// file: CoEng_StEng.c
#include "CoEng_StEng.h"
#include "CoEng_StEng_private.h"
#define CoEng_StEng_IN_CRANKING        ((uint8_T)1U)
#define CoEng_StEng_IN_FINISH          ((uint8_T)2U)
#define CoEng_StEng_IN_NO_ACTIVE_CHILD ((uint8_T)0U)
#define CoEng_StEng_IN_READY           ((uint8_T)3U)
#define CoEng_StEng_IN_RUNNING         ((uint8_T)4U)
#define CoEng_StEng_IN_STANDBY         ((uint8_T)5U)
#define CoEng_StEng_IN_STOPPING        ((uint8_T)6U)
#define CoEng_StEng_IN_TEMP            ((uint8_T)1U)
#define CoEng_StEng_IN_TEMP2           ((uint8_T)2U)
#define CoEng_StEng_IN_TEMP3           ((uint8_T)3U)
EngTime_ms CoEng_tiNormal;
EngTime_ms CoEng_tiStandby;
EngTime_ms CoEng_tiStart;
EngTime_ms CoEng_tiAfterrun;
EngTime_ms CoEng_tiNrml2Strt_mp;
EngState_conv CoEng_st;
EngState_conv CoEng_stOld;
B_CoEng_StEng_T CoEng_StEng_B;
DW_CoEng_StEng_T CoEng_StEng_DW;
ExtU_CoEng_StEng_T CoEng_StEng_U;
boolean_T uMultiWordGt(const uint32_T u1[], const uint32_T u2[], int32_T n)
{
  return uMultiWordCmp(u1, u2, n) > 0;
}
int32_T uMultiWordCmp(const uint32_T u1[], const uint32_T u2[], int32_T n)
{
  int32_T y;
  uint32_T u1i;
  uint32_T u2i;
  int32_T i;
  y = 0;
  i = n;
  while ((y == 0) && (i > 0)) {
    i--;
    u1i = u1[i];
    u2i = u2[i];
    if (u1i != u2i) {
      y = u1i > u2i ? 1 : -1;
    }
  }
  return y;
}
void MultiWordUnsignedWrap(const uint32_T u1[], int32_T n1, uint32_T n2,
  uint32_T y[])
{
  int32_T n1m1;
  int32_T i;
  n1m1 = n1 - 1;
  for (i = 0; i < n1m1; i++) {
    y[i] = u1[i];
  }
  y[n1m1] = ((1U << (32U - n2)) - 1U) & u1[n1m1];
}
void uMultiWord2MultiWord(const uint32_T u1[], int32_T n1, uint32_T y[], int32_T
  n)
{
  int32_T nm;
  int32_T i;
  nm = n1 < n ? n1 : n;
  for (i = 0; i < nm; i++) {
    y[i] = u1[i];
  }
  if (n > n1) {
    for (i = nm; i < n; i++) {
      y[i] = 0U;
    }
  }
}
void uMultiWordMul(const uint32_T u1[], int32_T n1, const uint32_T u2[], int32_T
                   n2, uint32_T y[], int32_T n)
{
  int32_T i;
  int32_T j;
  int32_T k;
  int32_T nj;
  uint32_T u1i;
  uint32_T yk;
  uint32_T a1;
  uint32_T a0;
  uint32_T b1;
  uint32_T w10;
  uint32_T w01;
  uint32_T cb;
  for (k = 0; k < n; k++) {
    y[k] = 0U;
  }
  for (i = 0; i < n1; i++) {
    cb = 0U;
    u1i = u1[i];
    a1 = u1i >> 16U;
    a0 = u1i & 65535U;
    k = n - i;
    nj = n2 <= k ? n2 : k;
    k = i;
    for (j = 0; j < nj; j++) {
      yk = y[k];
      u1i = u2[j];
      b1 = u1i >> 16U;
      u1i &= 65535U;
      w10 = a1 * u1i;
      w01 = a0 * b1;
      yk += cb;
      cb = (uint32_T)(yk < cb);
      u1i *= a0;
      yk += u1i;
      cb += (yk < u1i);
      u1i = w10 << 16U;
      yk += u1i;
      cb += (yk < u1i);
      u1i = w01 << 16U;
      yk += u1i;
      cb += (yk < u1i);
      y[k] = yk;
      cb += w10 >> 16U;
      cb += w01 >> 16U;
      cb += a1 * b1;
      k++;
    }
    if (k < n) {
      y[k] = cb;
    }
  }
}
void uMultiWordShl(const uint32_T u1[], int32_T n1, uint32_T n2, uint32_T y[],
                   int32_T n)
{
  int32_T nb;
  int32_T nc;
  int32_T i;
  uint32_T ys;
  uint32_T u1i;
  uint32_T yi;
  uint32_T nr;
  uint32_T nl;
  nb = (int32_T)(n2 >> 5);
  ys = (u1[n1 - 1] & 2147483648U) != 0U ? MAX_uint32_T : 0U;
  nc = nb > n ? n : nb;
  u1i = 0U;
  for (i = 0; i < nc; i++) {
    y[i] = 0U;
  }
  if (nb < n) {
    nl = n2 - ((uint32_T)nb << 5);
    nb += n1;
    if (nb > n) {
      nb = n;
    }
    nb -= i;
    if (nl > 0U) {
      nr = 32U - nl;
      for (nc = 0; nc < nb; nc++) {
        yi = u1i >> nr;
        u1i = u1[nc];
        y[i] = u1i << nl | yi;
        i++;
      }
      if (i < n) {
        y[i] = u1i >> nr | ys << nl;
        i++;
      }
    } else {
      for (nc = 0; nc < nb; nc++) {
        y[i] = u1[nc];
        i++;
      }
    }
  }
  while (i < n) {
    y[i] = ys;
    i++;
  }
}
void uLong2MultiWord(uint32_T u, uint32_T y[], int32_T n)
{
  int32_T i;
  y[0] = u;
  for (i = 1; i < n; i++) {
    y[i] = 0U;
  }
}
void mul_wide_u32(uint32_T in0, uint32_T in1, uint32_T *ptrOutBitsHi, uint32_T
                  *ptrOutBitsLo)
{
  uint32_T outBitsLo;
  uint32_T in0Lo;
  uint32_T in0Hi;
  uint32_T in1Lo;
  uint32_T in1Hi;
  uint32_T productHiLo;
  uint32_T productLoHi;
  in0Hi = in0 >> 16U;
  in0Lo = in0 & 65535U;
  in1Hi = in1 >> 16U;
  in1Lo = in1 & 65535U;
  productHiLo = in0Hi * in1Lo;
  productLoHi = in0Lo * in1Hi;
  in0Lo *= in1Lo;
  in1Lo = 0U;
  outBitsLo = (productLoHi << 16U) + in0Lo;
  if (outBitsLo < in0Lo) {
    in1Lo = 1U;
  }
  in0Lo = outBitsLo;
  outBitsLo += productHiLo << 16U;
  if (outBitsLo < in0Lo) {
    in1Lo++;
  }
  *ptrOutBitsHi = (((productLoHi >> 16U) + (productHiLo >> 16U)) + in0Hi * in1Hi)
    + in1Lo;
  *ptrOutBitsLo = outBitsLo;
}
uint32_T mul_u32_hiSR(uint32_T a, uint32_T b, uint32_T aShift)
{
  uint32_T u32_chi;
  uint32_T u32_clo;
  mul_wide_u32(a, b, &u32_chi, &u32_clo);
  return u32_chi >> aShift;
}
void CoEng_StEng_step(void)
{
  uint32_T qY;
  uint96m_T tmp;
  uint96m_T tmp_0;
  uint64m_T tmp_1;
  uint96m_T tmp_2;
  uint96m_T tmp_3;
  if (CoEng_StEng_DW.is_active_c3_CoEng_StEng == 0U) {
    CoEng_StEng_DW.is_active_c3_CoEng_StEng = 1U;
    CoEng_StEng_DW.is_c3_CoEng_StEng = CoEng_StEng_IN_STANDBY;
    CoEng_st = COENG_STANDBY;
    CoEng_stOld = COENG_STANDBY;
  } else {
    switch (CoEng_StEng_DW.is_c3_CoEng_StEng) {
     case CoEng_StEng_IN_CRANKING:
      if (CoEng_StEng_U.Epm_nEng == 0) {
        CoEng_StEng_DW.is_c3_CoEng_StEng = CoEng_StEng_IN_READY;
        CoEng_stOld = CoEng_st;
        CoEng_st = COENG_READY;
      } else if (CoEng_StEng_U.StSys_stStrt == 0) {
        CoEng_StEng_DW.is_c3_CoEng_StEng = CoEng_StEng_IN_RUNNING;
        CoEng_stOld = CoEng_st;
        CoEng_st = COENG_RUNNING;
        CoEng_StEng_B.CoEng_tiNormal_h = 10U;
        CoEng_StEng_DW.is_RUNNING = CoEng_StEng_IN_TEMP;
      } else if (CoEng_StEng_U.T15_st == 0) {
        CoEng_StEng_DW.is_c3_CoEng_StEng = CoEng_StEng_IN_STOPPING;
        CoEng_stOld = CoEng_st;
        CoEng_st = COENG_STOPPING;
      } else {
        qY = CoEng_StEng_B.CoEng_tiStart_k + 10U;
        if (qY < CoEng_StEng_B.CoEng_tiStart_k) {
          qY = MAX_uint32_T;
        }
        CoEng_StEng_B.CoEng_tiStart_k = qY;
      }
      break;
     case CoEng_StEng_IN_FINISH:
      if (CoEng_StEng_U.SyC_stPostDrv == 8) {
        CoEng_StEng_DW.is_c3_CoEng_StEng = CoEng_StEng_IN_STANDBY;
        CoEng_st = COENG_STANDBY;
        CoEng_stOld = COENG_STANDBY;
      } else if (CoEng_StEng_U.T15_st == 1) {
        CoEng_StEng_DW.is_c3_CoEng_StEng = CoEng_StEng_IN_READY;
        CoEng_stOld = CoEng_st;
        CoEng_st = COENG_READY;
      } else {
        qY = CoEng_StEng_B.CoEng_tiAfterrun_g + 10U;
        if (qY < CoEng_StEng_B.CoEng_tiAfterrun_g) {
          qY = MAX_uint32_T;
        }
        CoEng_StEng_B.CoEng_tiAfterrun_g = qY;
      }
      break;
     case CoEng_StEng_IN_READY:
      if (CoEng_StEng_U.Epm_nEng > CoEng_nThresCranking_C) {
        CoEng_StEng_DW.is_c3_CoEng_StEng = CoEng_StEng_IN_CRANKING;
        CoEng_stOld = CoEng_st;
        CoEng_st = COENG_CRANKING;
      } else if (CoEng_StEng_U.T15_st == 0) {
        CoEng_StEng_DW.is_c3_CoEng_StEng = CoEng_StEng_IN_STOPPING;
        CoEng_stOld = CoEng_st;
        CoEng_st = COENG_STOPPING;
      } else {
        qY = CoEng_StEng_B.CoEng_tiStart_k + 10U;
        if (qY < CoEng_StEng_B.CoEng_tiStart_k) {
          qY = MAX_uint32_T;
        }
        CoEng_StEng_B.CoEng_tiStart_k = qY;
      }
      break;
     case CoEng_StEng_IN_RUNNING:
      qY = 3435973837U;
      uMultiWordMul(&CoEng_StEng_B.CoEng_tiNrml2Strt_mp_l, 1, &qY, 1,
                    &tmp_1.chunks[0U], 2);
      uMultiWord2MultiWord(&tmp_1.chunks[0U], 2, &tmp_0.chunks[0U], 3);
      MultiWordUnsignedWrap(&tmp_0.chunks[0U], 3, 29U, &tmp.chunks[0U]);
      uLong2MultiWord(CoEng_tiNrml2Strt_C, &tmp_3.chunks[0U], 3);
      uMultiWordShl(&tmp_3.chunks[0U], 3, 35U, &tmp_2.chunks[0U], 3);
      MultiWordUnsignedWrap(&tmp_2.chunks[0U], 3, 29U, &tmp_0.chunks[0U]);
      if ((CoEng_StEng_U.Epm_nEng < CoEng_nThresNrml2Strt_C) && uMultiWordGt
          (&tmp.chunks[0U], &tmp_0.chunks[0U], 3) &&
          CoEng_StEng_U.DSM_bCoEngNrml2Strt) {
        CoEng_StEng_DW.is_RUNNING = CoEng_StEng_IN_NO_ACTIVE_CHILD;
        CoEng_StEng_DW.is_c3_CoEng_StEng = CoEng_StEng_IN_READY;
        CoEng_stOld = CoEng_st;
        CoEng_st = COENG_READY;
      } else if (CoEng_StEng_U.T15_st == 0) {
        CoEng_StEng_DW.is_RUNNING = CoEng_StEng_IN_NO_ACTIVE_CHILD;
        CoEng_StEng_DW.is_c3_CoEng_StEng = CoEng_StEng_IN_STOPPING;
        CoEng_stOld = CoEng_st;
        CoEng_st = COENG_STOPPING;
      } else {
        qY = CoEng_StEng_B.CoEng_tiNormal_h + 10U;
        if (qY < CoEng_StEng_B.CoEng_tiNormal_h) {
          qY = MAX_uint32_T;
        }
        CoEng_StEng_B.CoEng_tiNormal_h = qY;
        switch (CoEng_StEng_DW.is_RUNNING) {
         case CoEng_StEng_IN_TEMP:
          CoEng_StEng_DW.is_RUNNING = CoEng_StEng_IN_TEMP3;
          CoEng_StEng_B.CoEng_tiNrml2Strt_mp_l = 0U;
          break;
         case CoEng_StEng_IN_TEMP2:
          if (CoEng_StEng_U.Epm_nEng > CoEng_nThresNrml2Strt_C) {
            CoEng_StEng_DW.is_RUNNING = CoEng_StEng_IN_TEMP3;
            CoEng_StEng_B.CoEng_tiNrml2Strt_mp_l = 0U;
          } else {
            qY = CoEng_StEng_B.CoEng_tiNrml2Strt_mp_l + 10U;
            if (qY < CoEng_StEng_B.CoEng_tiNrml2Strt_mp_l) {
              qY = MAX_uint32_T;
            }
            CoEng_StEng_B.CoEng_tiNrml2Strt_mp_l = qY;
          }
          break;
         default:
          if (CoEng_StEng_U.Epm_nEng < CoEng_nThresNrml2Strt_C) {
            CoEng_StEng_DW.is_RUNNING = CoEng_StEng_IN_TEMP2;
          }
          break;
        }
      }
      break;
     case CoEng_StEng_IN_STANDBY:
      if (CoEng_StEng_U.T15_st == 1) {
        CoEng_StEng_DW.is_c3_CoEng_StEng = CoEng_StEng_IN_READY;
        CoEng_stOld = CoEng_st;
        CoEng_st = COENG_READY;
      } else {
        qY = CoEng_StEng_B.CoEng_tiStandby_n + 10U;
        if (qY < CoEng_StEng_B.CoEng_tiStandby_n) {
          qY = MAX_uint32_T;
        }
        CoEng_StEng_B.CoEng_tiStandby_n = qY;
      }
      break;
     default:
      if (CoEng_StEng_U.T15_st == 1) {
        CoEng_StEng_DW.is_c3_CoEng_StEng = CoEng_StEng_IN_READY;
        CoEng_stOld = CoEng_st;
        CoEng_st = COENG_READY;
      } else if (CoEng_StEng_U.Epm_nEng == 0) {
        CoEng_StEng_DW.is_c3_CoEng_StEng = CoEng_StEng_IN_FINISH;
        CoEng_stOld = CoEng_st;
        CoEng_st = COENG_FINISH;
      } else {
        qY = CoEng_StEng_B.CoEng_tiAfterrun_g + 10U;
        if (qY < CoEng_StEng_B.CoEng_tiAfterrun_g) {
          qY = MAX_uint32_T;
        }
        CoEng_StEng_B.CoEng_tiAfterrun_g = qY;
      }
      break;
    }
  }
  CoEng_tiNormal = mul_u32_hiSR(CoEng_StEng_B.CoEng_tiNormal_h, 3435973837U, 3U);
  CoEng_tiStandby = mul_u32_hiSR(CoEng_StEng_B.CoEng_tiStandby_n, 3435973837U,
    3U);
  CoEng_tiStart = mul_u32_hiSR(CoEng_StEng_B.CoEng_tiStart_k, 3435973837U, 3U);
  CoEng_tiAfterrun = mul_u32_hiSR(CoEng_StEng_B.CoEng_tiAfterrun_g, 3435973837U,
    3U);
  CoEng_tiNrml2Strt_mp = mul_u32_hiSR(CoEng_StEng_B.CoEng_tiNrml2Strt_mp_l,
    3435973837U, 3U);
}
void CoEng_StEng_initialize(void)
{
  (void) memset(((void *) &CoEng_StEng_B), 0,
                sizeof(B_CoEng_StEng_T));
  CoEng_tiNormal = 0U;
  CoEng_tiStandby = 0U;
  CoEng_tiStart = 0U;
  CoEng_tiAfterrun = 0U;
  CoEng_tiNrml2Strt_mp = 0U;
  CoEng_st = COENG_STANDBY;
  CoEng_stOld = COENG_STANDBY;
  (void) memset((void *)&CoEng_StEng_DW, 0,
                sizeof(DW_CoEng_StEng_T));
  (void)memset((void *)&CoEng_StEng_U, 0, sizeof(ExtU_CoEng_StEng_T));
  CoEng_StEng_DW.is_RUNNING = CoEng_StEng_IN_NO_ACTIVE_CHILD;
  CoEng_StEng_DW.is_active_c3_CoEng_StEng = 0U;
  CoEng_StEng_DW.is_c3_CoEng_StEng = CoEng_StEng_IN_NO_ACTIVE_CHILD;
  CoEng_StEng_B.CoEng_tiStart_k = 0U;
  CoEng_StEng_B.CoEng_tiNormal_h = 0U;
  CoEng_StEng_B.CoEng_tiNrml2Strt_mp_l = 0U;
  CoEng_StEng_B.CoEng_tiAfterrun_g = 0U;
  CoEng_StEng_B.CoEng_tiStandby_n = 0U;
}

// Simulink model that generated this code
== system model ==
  T15_st : Inport
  Epm_nEng : Inport
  StSys_stStrt : Inport
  SyC_stPostDrv : Inport
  DSM_bCoEngNrml2Strt : Inport
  TriggerPort#1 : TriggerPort  TriggerType=function-call
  CoEng_st : Outport  <- 1: Stateflowchart#1
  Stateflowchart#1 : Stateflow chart  <- 1: T15_st, 2: Epm_nEng, 3: StSys_stStrt, 4: SyC_stPostDrv, 5: Constant#1, 6: DSM_bCoEngNrml2Strt, 7: Constant#2, 8: Constant#3, 9: DataTypeConversion#1
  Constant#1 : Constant  Value=CoEng_nThresCranking_C
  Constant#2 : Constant  Value=CoEng_nThresNrml2Strt_C
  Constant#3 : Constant  Value=CoEng_tiNrml2Strt_C
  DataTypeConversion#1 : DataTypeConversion  <- 1: Constant#4
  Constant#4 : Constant  Value=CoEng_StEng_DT
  CoEng_stOld : Outport  <- 1: Stateflowchart#1/2
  CoEng_tiNormal : Outport  <- 1: DataTypeConversion#2
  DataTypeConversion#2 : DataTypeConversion  <- 1: Stateflowchart#1/4
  CoEng_tiStandby : Outport  <- 1: DataTypeConversion#3
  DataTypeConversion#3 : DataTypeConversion  <- 1: Stateflowchart#1/7
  CoEng_tiStart : Outport  <- 1: DataTypeConversion#4
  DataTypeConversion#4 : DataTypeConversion  <- 1: Stateflowchart#1/3
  CoEng_tiAfterrun : Outport  <- 1: DataTypeConversion#5
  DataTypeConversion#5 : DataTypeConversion  <- 1: Stateflowchart#1/6
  CoEng_tiNrml2Strt_mp : Outport  <- 1: DataTypeConversion#6
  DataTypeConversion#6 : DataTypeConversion  <- 1: Stateflowchart#1/5
== stateflow chart Stateflowchart#1 ==
  state STANDBY
    entry:
    CoEng_st=EngState_conv.COENG_STANDBY;
    CoEng_stOld=EngState_conv.COENG_STANDBY;
    during:
    CoEng_tiStandby=CoEng_tiStandby+DT;
  state READY
    entry:
    CoEng_stOld=CoEng_st;
    CoEng_st=EngState_conv.COENG_READY;
    during:
    CoEng_tiStart=CoEng_tiStart+DT;
  state FINISH
    entry:
    CoEng_stOld=CoEng_st;
    CoEng_st=EngState_conv.COENG_FINISH;
    during:
    CoEng_tiAfterrun=CoEng_tiAfterrun+DT;
  state STOPPING
    entry:
    CoEng_stOld=CoEng_st;
    CoEng_st=EngState_conv.COENG_STOPPING;
    during:
    CoEng_tiAfterrun=CoEng_tiAfterrun+DT;
  state CRANKING
    entry:
    CoEng_stOld=CoEng_st;
    CoEng_st=EngState_conv.COENG_CRANKING;
    during:
    CoEng_tiStart=CoEng_tiStart+DT;
  state RUNNING
    entry:
    CoEng_stOld=CoEng_st;
    CoEng_st=EngState_conv.COENG_RUNNING;
    CoEng_tiNormal=DT;
    during:
    CoEng_tiNormal=CoEng_tiNormal+DT;
    state TEMP2
      during:CoEng_tiNrml2Strt_mp = CoEng_tiNrml2Strt_mp + DT;
    state TEMP
    state TEMP3
      entry:CoEng_tiNrml2Strt_mp=uint32(0);
    (default) -> TEMP
    TEMP3 -> TEMP2 : [Epm_nEng<CoEng_nThresNrml2Strt_C]
    TEMP2 -> TEMP3 : [Epm_nEng>CoEng_nThresNrml2Strt_C]
    TEMP -> TEMP3
  (default) -> STANDBY
  STANDBY -> READY : [T15_st==1]
  FINISH -> STANDBY [order 1] : [SyC_stPostDrv==8]
  FINISH -> READY [order 2] : [T15_st==1]
  STOPPING -> READY [order 1] : [T15_st==1]
  RUNNING -> READY [order 1] : [(Epm_nEng<CoEng_nThresNrml2Strt_C)&&...
      | (CoEng_tiNrml2Strt_mp>CoEng_tiNrml2Strt_C)&&...
      | (DSM_bCoEng_Nrml2Strt==1)]
  READY -> STOPPING [order 2] : [T15_st==0]
  CRANKING -> READY [order 1] : [Epm_nEng==int16(0)]
  READY -> CRANKING [order 1] : [Epm_nEng>CoEng_nThresCranking_C]
  STOPPING -> FINISH [order 2] : [Epm_nEng==int16(0)]
  CRANKING -> STOPPING [order 3] : [T15_st==0]
  CRANKING -> RUNNING [order 2] : [StSys_stStrt==0]
  RUNNING -> STOPPING [order 2] : [T15_st==0]
  data: T15_st input; Epm_nEng input [0..12799]; StSys_stStrt input; SyC_stPostDrv input; CoEng_st output; CoEng_stOld output; CoEng_nThresCranking_C input [0..12799]; DSM_bCoEng_Nrml2Strt input [0..1]; CoEng_nThresNrml2Strt_C input [0..12799]; CoEng_tiNrml2Strt_C input [0..65535]; DT input uint32; CoEng_tiStart output uint32 size=1 =uint32(0); CoEng_tiNormal output uint32 size=1 =uint32(0); CoEng_tiNrml2Strt_mp output uint32 size=1 [0..65535] =uint32(0); CoEng_tiAfterrun output uint32 size=1 =uint32(0); CoEng_tiStandby output uint32 size=1 =uint32(0)
